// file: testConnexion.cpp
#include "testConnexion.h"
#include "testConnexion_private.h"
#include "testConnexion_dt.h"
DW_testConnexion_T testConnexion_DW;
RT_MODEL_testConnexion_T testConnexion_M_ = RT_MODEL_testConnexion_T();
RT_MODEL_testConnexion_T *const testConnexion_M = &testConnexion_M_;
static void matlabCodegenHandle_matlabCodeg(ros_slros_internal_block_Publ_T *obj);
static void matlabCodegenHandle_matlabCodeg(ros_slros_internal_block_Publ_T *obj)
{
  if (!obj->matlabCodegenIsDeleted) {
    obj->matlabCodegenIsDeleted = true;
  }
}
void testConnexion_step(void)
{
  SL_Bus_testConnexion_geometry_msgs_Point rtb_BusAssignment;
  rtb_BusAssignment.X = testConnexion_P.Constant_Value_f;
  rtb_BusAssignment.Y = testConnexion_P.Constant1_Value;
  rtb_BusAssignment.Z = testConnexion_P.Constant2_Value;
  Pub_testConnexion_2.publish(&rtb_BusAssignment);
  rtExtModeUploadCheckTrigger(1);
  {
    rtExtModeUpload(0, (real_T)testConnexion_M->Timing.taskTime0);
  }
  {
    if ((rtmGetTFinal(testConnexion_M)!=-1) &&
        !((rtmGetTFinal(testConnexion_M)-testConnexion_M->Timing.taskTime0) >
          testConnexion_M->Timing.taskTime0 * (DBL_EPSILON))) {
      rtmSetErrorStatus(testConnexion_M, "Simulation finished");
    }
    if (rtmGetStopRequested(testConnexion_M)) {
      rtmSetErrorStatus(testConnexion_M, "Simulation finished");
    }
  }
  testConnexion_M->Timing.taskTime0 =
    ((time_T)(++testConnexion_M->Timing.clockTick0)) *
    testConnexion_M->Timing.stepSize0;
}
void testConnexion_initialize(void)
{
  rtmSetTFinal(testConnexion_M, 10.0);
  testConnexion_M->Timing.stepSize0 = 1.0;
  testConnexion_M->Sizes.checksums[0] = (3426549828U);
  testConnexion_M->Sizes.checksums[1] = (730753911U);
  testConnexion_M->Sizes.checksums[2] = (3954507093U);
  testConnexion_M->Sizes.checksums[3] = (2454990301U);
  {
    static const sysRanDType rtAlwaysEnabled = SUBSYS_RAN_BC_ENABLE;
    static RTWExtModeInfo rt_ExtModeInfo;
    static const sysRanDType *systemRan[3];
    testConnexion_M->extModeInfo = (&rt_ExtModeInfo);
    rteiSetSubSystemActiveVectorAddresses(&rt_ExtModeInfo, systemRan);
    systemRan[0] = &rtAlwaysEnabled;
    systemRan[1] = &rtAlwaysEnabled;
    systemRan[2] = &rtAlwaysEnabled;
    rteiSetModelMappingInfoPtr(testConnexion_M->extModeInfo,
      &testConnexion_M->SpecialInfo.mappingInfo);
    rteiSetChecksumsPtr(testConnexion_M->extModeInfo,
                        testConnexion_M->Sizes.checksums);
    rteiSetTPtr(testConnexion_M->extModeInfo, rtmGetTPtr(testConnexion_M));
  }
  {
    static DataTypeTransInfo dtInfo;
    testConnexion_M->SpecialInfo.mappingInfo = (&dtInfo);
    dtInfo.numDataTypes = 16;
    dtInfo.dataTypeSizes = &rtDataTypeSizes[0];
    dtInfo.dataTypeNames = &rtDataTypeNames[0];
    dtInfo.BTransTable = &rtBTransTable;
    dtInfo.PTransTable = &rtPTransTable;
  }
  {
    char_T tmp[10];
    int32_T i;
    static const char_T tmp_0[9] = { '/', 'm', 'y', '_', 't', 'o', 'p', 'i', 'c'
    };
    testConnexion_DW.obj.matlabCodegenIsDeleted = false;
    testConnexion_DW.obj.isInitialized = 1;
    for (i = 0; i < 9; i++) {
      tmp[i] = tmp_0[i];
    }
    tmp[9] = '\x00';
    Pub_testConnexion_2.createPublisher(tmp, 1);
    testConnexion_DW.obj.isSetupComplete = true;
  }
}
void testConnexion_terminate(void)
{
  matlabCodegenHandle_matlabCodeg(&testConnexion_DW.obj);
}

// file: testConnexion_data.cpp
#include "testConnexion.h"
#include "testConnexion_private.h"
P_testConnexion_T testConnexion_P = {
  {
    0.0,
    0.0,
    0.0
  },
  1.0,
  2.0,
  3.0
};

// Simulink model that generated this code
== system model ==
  Publish#1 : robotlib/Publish  <- 1: BusAssignment
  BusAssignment : BusAssignment  <- 1: BlankMessage#1, 2: Constant, 3: Constant1, 4: Constant2
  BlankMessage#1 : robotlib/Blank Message
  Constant : Constant
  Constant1 : Constant  Value=2
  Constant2 : Constant  Value=3
